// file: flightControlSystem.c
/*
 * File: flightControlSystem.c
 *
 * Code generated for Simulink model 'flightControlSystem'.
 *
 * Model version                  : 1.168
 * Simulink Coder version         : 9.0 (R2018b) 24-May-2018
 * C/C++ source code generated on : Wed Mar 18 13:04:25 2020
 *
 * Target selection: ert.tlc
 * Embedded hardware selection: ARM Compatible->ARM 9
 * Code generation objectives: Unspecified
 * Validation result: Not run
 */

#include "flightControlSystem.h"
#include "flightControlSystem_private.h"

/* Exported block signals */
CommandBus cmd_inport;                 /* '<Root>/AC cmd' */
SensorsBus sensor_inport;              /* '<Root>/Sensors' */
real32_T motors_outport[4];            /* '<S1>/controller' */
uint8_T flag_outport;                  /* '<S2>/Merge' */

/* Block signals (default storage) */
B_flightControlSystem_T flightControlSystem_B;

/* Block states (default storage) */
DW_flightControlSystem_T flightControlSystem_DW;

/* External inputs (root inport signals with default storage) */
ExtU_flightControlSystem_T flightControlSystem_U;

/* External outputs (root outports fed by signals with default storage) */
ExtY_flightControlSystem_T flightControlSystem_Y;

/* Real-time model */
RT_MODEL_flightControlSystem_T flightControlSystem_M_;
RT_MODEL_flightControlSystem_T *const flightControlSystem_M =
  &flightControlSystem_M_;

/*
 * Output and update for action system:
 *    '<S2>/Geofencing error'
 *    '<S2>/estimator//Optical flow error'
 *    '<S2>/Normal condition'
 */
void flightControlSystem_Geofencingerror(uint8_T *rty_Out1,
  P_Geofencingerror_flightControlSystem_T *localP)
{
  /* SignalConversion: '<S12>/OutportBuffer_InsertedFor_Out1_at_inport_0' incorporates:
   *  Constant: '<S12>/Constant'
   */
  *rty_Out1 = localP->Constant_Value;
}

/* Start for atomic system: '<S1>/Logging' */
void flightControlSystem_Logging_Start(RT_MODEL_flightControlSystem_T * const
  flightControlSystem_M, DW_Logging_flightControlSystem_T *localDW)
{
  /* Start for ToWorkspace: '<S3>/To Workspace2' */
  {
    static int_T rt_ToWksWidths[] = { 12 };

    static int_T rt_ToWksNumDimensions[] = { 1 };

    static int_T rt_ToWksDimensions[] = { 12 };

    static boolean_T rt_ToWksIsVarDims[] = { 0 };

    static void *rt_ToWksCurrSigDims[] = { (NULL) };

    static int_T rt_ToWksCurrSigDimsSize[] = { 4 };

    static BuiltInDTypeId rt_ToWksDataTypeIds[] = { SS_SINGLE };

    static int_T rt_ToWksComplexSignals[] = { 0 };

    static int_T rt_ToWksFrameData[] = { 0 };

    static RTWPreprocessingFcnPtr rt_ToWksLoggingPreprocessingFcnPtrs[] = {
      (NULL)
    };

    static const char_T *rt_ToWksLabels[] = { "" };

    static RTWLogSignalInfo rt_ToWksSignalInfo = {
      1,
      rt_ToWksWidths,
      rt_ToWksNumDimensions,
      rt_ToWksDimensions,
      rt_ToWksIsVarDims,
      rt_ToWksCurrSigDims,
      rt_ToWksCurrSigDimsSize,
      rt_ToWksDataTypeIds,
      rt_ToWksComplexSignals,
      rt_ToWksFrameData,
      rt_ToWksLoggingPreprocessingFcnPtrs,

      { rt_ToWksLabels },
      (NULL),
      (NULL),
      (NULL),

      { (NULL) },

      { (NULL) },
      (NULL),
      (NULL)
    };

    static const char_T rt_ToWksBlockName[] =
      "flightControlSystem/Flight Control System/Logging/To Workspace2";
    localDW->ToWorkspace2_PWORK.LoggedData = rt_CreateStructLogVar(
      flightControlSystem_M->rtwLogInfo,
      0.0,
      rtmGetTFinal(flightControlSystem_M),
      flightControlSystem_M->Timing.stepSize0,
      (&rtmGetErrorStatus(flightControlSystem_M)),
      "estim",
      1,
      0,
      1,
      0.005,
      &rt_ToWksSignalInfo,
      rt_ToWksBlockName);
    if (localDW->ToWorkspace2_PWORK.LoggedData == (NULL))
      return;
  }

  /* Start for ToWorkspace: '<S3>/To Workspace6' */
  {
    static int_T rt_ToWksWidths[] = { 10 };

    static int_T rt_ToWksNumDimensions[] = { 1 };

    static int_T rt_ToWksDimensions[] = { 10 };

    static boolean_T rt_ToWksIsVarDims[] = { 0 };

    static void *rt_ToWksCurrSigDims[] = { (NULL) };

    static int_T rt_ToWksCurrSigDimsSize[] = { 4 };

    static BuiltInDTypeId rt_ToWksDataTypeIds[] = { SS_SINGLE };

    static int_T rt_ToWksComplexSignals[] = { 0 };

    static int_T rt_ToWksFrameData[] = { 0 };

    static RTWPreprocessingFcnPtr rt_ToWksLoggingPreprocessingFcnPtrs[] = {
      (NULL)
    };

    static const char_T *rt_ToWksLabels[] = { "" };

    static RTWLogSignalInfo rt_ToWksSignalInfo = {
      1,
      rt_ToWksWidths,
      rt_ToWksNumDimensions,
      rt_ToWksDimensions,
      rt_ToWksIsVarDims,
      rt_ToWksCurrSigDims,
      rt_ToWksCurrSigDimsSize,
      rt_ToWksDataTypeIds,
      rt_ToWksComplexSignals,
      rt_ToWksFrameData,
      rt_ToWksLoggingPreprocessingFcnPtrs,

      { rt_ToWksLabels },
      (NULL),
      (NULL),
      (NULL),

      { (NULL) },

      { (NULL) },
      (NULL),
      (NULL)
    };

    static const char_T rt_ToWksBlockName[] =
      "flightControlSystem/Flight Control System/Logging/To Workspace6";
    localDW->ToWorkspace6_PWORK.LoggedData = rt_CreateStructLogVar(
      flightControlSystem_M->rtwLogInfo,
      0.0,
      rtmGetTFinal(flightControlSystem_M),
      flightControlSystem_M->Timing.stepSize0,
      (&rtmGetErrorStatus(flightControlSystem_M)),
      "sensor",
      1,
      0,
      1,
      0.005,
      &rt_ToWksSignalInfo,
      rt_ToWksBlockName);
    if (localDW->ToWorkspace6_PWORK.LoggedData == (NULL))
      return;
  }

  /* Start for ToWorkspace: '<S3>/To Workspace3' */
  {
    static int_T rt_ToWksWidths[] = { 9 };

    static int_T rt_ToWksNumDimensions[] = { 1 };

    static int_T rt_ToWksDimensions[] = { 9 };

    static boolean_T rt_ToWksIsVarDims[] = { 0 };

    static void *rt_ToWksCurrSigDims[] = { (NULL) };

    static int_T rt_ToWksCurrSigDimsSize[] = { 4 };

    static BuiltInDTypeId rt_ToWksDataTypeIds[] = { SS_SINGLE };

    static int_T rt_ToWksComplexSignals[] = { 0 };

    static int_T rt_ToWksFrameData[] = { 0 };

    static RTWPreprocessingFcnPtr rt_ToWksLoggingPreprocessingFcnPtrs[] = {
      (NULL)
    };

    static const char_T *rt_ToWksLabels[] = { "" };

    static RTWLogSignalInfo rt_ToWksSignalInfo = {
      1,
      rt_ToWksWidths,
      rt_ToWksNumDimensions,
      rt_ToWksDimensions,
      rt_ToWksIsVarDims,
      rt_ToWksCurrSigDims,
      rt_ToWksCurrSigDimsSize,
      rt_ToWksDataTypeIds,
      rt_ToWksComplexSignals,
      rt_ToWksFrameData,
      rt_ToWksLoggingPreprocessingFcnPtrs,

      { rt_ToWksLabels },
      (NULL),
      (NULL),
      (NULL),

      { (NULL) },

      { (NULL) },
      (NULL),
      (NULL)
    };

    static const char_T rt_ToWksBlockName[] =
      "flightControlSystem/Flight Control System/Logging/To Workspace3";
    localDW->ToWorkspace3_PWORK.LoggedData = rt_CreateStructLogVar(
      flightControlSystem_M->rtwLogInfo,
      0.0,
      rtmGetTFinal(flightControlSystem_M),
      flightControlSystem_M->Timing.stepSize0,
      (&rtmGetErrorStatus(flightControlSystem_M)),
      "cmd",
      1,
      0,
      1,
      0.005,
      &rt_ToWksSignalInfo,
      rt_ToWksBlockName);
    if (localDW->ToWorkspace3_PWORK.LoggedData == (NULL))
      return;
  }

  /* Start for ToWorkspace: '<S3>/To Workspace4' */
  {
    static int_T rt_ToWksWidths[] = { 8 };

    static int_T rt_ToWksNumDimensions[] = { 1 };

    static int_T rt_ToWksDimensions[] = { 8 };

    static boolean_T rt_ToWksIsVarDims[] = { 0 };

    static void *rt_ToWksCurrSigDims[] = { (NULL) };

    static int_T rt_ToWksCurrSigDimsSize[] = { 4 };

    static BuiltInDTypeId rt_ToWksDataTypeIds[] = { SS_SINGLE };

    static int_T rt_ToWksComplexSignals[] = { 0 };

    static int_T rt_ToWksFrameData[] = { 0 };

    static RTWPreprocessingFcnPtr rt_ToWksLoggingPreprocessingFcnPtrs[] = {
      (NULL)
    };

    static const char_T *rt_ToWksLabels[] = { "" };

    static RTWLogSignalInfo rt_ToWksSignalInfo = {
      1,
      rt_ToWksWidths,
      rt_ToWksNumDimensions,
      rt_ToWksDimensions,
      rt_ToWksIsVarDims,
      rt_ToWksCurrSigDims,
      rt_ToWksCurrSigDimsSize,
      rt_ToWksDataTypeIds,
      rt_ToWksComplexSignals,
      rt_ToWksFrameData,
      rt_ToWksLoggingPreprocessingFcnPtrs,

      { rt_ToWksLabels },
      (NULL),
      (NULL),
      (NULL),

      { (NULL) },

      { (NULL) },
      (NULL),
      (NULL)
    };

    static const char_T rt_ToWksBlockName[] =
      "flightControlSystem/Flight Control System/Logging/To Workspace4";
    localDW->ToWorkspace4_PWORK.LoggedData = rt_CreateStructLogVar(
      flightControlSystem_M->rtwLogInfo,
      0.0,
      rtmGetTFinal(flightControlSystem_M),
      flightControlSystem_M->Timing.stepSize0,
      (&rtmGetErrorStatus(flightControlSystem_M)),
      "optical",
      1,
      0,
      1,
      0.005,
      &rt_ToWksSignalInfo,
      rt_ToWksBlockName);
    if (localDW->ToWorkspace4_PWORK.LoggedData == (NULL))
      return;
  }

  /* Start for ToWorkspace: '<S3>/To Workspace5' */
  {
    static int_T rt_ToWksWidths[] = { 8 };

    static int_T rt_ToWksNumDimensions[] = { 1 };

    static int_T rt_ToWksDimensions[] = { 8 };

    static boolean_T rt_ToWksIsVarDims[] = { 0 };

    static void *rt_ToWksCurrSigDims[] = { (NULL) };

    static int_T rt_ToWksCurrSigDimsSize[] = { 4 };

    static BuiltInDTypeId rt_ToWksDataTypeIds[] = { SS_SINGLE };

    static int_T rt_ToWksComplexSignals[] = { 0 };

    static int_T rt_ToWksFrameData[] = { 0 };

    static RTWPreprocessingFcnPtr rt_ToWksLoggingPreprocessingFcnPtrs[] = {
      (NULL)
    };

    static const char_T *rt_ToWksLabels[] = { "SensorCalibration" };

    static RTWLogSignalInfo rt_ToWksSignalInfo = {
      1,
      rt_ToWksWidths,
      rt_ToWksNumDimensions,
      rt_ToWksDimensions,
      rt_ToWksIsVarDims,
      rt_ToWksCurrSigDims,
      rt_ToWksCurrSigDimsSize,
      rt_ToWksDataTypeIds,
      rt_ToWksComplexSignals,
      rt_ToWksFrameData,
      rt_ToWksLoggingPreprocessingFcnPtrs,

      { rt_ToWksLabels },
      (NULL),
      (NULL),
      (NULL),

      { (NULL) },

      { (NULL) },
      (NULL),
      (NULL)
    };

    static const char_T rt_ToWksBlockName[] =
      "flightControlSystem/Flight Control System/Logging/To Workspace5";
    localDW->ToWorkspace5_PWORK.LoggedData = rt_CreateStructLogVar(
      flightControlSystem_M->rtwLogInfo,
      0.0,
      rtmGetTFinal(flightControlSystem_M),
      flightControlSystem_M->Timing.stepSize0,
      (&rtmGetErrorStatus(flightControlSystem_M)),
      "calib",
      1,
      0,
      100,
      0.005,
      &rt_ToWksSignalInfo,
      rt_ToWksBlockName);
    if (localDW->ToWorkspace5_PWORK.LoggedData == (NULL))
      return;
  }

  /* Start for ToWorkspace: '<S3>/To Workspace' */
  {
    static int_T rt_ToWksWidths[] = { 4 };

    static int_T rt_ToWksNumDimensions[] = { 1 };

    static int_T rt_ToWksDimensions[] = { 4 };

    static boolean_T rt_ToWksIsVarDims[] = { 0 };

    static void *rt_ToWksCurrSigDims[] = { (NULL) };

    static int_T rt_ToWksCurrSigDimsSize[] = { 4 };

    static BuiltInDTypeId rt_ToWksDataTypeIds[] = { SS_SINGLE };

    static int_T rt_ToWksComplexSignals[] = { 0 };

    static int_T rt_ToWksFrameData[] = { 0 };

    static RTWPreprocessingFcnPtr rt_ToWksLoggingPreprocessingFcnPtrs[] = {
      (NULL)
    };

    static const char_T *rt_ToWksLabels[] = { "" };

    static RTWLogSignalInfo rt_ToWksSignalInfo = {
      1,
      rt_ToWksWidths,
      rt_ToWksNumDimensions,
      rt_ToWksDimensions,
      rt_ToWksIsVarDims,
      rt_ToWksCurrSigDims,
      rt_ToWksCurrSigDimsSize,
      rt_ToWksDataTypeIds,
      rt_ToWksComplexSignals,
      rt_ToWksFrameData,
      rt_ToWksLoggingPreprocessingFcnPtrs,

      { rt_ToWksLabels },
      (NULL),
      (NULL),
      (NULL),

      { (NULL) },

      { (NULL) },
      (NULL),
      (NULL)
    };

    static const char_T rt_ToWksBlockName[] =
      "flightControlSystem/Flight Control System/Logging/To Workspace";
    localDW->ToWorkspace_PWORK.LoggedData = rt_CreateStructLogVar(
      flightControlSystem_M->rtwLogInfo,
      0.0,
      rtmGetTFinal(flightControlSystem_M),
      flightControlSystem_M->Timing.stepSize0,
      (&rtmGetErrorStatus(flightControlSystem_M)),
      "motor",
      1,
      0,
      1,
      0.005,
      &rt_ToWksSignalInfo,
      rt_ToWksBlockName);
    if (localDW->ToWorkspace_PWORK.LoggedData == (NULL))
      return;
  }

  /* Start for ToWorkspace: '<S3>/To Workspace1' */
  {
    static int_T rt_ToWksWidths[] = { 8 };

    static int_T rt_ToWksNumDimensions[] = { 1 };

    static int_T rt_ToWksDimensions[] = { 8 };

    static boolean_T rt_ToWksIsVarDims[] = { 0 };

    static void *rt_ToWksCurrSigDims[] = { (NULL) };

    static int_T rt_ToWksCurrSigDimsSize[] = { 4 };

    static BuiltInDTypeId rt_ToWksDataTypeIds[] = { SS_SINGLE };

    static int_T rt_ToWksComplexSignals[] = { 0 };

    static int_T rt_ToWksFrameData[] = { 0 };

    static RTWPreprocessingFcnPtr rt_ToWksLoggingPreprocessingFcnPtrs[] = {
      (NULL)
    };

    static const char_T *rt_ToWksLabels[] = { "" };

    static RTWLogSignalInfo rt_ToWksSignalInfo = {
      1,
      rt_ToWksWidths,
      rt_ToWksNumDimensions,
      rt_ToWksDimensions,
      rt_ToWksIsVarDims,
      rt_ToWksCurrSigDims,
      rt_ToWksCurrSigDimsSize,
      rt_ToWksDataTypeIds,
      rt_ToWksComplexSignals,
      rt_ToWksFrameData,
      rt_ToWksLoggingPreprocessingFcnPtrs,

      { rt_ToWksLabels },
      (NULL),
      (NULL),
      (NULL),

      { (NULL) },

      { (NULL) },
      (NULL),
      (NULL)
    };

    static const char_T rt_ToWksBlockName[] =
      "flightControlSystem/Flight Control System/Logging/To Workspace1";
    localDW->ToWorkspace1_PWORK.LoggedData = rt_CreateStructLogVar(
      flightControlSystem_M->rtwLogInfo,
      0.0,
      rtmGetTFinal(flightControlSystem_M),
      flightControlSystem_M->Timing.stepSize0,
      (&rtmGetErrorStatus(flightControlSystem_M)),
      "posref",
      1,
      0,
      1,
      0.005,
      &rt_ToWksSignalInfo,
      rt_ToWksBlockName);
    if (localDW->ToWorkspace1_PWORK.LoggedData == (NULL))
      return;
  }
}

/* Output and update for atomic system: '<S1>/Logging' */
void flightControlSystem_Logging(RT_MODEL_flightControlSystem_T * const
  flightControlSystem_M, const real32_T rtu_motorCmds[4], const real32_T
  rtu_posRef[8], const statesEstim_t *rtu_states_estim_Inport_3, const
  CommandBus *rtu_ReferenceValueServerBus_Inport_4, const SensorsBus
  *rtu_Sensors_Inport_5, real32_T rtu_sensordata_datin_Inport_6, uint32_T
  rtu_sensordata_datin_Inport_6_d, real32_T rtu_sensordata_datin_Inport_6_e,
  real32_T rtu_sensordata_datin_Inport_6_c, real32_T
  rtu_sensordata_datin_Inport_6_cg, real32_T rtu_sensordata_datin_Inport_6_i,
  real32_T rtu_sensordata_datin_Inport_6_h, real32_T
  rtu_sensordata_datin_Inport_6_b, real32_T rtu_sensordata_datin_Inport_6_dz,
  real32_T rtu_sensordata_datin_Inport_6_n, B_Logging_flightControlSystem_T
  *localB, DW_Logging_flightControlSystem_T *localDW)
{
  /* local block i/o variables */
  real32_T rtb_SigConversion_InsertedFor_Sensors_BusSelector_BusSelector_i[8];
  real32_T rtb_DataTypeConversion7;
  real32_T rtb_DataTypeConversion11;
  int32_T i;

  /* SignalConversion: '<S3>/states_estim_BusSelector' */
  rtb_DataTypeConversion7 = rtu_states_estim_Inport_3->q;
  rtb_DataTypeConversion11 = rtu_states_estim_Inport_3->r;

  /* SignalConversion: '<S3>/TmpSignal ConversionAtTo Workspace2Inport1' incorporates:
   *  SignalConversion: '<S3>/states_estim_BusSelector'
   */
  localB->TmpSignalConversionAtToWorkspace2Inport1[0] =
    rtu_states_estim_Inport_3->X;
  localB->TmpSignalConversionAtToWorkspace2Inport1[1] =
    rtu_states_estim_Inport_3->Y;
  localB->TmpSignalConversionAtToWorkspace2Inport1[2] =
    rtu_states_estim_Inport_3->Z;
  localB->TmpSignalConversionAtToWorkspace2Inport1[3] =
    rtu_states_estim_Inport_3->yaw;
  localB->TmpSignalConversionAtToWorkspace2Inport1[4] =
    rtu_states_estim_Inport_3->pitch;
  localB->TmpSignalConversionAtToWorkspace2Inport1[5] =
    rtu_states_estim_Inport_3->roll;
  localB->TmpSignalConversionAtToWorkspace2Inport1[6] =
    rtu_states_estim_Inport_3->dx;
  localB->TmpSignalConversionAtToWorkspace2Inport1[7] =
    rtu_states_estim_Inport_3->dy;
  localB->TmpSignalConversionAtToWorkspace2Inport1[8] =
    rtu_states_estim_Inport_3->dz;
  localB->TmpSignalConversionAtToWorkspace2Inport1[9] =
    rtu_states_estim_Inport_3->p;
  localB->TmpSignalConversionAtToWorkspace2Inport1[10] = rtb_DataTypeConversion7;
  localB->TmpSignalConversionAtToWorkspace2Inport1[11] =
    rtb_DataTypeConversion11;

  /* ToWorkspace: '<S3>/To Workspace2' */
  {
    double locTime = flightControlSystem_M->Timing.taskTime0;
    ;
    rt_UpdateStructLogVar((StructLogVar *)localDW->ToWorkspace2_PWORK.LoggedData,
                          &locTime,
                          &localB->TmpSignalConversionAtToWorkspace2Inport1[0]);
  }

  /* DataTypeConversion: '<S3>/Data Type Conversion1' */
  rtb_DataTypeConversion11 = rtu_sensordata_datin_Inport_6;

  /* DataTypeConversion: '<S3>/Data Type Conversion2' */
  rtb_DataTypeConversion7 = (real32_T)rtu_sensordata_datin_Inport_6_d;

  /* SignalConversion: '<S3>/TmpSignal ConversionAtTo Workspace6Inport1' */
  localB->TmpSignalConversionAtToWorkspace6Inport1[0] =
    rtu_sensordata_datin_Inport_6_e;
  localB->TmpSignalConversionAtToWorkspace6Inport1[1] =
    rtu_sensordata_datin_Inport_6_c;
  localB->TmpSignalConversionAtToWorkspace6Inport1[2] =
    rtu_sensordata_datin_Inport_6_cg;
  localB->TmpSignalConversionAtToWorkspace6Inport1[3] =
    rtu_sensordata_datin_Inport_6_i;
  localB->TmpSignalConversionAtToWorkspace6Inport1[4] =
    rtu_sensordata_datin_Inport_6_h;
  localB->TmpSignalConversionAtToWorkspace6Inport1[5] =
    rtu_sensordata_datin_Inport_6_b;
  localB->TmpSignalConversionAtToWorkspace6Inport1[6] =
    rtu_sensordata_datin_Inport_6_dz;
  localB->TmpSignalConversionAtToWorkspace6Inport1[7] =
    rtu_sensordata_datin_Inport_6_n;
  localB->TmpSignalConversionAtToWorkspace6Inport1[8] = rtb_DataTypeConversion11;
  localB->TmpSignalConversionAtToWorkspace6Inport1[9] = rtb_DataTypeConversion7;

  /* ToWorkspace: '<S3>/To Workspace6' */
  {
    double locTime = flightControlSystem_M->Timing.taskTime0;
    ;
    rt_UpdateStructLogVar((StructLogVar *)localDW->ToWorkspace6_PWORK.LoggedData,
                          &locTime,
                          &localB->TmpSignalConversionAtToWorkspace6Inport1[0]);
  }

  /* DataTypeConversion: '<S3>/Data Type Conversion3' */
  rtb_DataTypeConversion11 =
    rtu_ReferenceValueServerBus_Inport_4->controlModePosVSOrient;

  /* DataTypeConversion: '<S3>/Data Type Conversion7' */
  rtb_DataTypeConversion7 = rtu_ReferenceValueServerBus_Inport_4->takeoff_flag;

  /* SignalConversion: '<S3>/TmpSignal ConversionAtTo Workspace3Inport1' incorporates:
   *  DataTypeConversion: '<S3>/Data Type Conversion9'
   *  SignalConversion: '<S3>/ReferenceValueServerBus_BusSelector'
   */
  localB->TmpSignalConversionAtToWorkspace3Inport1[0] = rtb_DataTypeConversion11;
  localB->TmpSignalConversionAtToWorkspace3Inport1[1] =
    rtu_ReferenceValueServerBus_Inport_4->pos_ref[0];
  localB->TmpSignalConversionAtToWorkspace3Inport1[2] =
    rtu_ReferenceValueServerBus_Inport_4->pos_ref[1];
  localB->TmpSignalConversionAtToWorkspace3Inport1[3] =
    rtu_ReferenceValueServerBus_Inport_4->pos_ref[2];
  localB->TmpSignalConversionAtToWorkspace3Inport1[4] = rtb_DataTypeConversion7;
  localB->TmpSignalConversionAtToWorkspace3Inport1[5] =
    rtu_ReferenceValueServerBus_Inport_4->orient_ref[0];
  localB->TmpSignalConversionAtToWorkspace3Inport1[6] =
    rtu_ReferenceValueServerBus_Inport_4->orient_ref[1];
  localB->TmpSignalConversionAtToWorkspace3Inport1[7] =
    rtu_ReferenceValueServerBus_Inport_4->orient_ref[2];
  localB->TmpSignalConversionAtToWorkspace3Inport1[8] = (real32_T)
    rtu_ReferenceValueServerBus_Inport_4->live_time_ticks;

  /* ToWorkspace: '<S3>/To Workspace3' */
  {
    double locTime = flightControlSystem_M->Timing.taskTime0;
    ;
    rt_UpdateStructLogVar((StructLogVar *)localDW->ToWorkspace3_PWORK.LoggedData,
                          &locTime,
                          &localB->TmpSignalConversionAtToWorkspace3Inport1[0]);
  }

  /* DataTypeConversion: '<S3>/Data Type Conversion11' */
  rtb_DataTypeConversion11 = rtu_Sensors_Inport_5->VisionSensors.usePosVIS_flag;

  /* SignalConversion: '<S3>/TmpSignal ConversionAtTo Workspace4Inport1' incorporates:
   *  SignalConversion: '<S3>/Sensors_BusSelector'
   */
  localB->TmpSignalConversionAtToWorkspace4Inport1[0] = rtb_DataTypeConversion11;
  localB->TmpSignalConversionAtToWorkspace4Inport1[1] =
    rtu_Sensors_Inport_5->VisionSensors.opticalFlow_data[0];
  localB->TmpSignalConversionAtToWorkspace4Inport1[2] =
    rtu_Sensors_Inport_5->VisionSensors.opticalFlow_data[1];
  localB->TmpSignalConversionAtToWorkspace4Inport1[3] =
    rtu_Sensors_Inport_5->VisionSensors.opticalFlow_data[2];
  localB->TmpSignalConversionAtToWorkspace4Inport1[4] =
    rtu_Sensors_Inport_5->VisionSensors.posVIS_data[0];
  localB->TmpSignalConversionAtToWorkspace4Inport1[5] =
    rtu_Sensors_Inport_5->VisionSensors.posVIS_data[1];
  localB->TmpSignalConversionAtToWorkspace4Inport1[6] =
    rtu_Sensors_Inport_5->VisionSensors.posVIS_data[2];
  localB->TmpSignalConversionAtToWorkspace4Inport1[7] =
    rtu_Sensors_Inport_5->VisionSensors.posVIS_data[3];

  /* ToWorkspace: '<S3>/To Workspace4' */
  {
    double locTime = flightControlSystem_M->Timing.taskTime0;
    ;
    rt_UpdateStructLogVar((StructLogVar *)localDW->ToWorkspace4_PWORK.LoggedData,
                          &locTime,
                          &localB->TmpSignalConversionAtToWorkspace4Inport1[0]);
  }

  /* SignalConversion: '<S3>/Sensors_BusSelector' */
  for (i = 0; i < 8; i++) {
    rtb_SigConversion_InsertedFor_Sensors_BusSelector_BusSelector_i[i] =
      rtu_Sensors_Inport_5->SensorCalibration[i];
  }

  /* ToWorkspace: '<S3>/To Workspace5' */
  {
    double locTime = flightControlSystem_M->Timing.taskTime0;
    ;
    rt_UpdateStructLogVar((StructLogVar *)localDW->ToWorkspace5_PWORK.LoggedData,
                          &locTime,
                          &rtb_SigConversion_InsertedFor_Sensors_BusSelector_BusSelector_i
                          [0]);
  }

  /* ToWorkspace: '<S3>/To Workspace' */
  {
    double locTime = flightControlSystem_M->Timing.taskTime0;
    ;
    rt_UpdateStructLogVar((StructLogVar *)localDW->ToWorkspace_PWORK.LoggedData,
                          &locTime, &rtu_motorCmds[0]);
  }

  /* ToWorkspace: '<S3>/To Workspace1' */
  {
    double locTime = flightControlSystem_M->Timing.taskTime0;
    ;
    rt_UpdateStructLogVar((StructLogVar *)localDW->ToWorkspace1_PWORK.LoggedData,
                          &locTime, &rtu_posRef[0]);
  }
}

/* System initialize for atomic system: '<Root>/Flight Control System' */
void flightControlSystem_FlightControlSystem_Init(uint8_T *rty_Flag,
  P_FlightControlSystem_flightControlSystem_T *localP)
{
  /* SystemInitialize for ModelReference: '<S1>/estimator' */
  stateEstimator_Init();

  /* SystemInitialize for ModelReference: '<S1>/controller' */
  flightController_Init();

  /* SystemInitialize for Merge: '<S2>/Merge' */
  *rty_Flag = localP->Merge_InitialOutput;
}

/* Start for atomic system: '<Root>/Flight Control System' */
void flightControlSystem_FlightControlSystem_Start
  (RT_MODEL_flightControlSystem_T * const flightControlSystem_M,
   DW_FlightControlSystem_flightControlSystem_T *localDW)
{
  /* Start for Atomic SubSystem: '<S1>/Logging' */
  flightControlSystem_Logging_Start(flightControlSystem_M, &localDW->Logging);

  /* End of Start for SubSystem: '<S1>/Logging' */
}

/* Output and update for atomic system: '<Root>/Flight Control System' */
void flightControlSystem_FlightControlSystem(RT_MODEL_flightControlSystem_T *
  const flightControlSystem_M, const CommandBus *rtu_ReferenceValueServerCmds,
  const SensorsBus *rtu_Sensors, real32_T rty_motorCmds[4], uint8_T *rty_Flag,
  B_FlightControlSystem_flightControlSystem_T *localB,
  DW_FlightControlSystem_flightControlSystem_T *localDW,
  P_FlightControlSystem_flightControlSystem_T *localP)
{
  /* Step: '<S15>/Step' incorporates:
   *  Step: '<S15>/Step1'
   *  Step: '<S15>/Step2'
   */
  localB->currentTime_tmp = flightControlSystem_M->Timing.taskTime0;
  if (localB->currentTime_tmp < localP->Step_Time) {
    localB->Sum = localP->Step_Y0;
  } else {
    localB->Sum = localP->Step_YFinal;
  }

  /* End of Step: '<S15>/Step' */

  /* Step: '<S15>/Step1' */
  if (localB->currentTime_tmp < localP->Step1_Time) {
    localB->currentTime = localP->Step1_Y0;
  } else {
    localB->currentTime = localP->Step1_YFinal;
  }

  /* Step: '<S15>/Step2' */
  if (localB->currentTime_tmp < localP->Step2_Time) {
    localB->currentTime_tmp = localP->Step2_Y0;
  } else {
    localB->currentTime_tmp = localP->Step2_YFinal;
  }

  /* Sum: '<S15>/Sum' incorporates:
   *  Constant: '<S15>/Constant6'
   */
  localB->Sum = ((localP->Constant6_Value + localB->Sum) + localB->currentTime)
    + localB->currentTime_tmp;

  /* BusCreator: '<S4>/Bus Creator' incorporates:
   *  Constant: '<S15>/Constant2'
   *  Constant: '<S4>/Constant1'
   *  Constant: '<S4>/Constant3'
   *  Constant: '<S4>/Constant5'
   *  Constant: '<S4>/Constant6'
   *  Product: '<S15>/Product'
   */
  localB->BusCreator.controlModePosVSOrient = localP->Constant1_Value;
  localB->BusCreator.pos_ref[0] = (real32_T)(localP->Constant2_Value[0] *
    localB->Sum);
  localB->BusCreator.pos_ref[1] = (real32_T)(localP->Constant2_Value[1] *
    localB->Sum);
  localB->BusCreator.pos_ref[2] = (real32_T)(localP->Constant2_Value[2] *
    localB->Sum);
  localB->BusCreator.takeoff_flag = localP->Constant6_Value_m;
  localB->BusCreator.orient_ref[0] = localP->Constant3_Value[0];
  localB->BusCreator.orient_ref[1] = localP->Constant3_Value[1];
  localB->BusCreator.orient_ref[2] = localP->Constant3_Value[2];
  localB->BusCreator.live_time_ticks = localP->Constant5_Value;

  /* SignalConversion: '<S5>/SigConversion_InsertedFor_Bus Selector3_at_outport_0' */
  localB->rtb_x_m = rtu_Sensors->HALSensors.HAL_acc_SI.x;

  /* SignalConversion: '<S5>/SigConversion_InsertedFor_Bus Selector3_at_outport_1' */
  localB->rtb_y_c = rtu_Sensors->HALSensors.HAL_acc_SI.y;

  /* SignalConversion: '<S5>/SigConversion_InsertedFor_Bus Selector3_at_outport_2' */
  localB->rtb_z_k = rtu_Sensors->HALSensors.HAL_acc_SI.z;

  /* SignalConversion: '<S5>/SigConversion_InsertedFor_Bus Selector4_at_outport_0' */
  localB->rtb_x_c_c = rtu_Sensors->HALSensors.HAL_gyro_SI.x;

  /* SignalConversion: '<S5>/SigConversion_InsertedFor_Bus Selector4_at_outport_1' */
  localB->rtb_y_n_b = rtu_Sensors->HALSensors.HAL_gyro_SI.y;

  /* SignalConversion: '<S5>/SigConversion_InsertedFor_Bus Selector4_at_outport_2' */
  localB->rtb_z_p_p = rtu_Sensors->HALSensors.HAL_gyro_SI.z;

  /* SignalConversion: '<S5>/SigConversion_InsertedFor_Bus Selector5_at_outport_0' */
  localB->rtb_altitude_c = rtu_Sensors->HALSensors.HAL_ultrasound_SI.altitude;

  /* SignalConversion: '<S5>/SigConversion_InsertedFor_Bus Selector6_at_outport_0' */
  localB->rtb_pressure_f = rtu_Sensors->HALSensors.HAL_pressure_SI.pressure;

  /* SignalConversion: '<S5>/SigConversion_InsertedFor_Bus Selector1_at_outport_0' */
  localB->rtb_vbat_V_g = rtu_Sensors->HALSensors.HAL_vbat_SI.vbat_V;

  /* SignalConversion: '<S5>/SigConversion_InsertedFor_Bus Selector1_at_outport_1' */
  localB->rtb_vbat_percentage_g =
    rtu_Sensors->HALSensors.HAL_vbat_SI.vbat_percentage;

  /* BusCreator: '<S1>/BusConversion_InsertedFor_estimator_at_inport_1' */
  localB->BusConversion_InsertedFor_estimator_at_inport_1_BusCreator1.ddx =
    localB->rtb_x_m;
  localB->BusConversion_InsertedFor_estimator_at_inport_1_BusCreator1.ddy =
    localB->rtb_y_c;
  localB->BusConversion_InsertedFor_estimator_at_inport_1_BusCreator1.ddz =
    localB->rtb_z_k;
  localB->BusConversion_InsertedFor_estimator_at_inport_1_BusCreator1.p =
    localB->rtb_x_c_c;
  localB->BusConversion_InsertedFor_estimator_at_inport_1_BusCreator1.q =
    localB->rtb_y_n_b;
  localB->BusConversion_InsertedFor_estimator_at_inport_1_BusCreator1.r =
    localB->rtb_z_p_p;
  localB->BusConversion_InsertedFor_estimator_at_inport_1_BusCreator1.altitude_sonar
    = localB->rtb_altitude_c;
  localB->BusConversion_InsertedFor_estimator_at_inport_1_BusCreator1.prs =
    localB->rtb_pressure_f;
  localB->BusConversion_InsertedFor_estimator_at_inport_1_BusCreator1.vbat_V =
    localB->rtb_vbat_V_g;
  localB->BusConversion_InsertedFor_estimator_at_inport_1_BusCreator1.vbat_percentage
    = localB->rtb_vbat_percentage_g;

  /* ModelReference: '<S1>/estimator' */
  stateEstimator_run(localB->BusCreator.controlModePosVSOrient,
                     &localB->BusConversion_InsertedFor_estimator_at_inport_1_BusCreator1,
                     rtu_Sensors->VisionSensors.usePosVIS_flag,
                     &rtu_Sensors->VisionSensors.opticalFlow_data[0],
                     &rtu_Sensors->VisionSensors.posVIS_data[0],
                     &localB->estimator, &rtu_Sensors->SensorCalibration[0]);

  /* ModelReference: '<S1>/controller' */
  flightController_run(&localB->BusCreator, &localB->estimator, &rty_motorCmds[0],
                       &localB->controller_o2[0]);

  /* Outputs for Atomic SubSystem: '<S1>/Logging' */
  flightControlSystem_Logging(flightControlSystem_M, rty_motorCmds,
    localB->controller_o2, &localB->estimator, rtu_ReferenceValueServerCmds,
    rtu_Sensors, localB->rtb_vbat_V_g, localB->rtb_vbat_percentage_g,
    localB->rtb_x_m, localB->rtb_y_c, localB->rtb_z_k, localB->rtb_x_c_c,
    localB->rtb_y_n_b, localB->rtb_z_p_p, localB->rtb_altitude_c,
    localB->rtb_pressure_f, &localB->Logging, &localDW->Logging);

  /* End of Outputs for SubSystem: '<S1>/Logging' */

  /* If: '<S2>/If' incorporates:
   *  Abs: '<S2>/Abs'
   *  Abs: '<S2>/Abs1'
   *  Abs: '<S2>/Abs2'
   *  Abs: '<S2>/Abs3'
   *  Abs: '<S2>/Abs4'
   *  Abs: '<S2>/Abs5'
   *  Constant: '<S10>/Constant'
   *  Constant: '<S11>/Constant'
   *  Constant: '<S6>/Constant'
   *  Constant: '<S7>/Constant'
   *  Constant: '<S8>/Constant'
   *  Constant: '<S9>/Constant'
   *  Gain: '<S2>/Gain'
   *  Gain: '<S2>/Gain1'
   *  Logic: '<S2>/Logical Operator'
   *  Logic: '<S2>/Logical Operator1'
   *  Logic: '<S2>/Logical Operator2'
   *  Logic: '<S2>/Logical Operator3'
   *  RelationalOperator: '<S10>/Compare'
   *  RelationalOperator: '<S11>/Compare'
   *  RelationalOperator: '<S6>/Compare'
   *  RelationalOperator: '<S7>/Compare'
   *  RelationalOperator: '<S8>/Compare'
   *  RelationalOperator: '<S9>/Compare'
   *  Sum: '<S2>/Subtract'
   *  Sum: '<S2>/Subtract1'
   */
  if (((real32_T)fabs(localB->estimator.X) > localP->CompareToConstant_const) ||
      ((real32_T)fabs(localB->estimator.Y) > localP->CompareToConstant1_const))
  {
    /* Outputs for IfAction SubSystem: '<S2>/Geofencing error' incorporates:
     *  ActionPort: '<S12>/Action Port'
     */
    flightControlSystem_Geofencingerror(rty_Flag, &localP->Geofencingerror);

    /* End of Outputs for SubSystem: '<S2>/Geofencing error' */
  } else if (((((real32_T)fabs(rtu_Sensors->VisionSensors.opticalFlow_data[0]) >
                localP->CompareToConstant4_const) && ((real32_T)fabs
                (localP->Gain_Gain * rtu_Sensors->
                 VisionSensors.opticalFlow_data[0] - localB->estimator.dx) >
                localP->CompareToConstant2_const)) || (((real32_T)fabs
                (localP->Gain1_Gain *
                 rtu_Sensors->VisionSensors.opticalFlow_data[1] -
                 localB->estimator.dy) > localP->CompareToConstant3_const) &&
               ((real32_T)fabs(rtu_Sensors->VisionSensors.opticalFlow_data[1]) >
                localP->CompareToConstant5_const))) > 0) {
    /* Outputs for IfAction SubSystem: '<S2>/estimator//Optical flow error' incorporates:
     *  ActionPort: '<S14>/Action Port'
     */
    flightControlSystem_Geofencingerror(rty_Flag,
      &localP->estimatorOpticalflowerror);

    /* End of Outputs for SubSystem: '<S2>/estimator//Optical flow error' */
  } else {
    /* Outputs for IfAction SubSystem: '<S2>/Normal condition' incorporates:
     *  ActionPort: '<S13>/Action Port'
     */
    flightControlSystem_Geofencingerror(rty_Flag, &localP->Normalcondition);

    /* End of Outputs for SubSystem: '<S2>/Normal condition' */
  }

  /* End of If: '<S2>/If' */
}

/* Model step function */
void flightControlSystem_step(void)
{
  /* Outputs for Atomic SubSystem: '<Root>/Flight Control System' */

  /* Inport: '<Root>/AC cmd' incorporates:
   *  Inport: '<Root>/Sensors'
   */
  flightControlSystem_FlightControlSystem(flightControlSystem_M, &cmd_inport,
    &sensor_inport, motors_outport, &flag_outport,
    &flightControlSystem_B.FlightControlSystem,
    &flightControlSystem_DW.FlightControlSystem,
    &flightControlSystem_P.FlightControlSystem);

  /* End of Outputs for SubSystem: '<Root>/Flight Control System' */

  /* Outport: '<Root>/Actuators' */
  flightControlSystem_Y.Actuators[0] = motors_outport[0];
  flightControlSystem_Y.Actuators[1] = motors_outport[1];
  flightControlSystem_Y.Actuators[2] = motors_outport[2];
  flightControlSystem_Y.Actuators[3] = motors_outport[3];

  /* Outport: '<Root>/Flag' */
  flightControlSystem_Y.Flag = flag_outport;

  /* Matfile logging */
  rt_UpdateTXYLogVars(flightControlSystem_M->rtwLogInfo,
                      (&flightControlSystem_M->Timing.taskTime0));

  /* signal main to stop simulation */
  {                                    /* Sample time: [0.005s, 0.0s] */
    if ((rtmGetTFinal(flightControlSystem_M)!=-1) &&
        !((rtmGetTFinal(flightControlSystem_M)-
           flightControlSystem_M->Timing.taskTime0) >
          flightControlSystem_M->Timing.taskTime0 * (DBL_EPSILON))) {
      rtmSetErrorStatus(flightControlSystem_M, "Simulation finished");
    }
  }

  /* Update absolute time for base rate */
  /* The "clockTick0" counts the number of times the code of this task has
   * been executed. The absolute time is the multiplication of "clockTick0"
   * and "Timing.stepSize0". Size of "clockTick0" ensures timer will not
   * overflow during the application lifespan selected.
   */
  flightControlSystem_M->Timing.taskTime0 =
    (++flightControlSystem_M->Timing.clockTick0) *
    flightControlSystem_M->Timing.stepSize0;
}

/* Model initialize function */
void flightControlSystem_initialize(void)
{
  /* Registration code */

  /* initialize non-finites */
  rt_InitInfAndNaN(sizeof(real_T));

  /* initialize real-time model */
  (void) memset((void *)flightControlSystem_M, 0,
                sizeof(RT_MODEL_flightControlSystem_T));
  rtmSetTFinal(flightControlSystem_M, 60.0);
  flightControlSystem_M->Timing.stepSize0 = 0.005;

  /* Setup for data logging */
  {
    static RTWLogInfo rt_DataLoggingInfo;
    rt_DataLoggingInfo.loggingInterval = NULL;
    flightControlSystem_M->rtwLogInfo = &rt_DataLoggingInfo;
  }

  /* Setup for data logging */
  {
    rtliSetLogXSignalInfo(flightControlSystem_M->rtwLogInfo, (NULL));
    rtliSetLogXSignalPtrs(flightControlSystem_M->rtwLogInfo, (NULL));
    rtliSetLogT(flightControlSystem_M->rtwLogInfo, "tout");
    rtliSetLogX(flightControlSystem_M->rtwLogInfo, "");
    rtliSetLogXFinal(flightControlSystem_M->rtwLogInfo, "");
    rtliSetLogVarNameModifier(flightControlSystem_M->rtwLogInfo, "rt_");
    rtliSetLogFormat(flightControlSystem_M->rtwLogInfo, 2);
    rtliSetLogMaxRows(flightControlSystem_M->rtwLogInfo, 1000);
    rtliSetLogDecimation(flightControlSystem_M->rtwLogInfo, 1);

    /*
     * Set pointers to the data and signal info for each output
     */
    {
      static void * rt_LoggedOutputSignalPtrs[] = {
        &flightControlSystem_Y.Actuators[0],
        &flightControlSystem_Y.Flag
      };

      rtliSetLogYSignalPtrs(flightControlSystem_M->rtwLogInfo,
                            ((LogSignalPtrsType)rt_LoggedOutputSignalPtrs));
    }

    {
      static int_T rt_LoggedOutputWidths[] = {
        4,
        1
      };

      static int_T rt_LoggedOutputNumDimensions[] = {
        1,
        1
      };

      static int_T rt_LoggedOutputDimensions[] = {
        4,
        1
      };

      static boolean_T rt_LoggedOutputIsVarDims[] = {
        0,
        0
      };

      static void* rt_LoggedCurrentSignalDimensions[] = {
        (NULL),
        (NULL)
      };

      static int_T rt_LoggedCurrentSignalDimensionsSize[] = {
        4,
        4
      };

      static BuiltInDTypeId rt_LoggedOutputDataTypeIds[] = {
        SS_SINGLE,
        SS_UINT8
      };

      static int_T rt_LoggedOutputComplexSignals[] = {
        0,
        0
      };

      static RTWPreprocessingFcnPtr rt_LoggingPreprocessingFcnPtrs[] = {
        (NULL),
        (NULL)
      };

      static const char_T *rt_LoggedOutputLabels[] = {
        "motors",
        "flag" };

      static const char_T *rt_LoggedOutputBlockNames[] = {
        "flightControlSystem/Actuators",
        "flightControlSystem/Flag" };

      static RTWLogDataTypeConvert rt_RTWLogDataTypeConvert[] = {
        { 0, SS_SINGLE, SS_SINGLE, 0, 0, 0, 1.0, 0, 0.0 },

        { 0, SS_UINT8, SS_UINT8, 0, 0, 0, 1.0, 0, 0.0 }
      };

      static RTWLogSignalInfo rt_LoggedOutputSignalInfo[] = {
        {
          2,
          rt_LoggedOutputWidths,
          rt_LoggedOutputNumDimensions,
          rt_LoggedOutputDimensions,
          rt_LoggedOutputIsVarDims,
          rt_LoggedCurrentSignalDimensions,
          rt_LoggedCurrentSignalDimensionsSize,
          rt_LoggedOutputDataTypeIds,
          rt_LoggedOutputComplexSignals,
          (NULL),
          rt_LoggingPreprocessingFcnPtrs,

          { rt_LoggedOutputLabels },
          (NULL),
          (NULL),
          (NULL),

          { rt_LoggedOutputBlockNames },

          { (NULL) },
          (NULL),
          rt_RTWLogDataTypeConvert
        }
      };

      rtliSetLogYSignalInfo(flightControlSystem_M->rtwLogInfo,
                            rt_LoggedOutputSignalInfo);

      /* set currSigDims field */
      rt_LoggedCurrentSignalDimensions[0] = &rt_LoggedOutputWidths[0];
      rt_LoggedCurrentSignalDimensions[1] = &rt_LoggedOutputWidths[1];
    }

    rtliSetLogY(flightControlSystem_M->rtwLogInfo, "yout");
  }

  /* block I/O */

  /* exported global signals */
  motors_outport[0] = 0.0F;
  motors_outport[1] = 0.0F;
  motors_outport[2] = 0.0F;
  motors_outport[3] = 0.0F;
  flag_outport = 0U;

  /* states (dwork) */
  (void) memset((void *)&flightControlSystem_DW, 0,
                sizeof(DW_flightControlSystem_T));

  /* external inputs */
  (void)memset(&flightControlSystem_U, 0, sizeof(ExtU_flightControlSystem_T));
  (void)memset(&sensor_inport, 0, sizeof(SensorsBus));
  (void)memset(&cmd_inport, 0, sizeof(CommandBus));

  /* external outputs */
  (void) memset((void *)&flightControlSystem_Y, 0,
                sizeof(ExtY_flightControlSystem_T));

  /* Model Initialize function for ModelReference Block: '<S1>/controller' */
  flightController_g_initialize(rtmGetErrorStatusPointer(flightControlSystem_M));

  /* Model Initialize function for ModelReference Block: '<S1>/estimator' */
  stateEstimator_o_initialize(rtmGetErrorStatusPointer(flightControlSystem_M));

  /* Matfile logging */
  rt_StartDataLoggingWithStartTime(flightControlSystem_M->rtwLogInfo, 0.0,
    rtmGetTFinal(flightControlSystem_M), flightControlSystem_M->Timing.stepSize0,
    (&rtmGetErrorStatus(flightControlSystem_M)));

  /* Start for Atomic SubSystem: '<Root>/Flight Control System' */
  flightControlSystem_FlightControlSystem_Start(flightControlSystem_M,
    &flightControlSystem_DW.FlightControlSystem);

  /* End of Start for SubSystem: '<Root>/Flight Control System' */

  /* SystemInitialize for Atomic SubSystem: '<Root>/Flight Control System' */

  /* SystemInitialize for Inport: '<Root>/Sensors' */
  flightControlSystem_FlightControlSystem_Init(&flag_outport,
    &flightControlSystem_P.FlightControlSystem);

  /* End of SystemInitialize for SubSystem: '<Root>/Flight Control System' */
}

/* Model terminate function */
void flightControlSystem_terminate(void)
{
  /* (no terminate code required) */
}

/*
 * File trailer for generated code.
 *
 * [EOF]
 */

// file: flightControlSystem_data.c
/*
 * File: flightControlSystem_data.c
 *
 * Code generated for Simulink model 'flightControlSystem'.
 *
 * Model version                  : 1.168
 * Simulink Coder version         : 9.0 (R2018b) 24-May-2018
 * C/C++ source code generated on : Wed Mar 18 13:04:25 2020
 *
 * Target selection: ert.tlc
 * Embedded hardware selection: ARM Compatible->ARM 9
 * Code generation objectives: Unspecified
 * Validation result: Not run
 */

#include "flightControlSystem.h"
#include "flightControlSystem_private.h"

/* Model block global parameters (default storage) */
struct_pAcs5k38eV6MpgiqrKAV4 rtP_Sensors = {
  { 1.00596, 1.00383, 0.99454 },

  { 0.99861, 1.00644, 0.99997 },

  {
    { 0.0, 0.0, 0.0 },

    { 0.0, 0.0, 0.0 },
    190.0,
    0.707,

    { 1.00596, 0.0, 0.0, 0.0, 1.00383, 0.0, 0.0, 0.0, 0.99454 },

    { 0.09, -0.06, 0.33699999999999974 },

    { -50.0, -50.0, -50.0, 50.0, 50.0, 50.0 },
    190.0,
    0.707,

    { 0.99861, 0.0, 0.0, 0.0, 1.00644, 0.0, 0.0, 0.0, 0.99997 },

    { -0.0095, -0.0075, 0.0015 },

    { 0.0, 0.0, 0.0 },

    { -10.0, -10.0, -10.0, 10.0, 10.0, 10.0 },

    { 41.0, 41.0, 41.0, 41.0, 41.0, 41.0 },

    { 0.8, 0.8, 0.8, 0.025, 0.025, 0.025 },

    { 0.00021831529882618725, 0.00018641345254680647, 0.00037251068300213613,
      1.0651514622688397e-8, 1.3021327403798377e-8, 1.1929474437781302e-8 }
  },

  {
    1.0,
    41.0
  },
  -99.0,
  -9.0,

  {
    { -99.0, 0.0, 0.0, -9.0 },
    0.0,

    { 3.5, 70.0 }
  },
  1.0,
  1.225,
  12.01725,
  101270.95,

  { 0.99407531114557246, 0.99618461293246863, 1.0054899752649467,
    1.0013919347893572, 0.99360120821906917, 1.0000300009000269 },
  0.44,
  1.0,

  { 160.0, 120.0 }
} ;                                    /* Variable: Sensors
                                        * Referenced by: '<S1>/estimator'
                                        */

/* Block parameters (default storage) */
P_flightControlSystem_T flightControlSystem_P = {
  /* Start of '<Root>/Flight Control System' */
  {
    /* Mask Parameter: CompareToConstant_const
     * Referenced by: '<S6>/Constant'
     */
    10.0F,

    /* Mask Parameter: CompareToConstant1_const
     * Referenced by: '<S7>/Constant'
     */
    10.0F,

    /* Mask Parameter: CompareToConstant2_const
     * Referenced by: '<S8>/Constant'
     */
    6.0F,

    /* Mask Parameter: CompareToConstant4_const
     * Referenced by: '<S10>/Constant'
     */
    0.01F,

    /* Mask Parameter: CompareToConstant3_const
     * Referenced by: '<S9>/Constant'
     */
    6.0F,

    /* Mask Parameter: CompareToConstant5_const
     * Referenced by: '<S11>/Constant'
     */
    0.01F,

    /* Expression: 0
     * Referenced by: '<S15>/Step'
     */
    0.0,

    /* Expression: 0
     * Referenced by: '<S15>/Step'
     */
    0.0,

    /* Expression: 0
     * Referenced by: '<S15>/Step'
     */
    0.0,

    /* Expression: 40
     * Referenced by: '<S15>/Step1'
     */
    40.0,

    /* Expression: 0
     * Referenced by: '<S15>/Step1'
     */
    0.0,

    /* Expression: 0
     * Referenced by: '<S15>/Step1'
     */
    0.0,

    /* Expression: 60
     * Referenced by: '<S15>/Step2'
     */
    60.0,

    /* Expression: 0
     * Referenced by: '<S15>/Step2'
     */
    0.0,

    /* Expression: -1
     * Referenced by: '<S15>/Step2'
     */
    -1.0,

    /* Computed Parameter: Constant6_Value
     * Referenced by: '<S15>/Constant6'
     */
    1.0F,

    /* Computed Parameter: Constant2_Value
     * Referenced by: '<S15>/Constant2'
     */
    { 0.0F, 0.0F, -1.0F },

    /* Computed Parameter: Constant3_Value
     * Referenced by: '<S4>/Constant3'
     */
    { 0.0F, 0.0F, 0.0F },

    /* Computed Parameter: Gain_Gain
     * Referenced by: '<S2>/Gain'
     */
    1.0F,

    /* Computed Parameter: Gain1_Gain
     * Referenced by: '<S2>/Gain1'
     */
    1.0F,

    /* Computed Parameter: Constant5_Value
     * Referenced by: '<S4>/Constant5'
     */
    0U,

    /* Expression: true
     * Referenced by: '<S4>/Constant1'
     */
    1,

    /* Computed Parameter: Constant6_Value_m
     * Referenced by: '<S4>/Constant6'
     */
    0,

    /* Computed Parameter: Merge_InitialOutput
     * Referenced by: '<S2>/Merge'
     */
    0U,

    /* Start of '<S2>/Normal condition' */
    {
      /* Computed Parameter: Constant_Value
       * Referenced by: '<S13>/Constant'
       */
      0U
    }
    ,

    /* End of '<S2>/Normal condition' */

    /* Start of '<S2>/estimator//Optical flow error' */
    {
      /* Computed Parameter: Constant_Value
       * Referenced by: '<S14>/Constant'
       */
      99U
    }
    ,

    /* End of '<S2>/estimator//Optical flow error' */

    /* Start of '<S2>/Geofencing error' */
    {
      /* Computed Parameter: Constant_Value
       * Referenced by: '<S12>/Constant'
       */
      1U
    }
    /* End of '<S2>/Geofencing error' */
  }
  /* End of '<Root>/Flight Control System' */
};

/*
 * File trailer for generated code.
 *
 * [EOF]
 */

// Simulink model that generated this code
simulink model "flightControlSystem"  (R2018b)
settings: Solver=ode3  StartTime=0  StopTime=60  FixedStep=Ts  RelTol=1e-3  EnableMultiTasking=on
undefined symbols (not defined in the file): Estimator, Ts
libraries: simulink x6

== system flightControlSystem ==
  note: Copyright 2013-2018 The MathWorks, Inc.
  note: Flight Control System
  AC cmd : Inport  OutDataTypeStr=Bus: CommandBus  BusOutputAsStruct=on
  Sensors : Inport  Port=2  OutDataTypeStr=Bus: SensorsBus  BusOutputAsStruct=on
  Image Data : Inport  Tag=IP_IN  Port=3  OutDataTypeStr=uint8  PortDimensions=[4 9600]  BusOutputAsStruct=on
  Flight Control System : Subsystem  TreatAsAtomicUnit=on  SystemSampleTime=Ts
  Terminator : Terminator
  Actuators : Outport  OutDataTypeStr=single  PortDimensions=4
  Flag : Outport  Port=2  OutDataTypeStr=uint8  PortDimensions=1
  wires:
  AC cmd/1 -> Flight Control System/1(ReferenceValueServerCmds)  "cmd"
  Flight Control System/1(motorCmds) -> Actuators/1  "motors"
  Sensors/1 -> Flight Control System/2(Sensors)  "sensors"
  Flight Control System/2(Flag) -> Flag/1  "flag"
  Image Data/1 -> Terminator/1  "Y1UY2V"

== system flightControlSystem/Flight Control System ==
  note: Derived from the work by Sertac
      | Karaman and Fabian Riether
  ReferenceValueServerCmds : Inport  OutDataTypeStr=Bus: CommandBus
  Sensors : Inport  Port=2  OutDataTypeStr=Bus: SensorsBus  BusOutputAsStruct=on
  Bus Selector : BusSelector  OutputSignals=VisionSensors.usePosVIS_flag,VisionSensors.opticalFlow_data,VisionSensors.posVIS_data,SensorCalibration
  Bus Selector1 : BusSelector  OutputSignals=controlModePosVSOrient
  Bus Selector2 : BusSelector  OutputSignals=HAL_acc_SI,HAL_gyro_SI,HAL_ultrasound_SI,HAL_pressure_SI,HAL_vbat_SI
  Bus Selector3 : BusSelector  OutputSignals=HALSensors
  Crash Predictor Flags : Subsystem
  Logging : Subsystem  TreatAsAtomicUnit=on
  Sensors1 : InportShadow  Port=2  OutDataTypeStr=Bus: SensorsBus  BusOutputAsStruct=on
  Sensors2 : InportShadow  Port=2  OutDataTypeStr=Bus: SensorsBus  BusOutputAsStruct=on
  Sensors3 : InportShadow  Port=2  OutDataTypeStr=Bus: SensorsBus  BusOutputAsStruct=on
  controller : ModelReference  ModelNameDialog=flightController.slx  SimulationMode=Normal  ModelReferenceVersion=1.361
  estimator : ModelReference  ModelNameDialog=stateEstimator.slx  SimulationMode=Normal  ModelReferenceVersion=1.43
  landing logic : Subsystem
  sensordata_group : Subsystem
  motorCmds : Outport
  Flag : Outport  Port=2
  wires:
  Bus Selector2/1 -> sensordata_group/1(HAL_acc_SI)  "<HAL_acc_SI>"
  Bus Selector2/2 -> sensordata_group/2(HAL_gyro_SI)  "<HAL_gyro_SI>"
  Bus Selector2/4 -> sensordata_group/4(HAL_pressure_SI)  "<HAL_pressure_SI>"
  Bus Selector2/3 -> sensordata_group/3(HAL_ultrasound_SI)  "<HAL_ultrasound_SI>"
  estimator/1 -> Crash Predictor Flags/1(states_estim), Logging/3(states_estim), controller/2
  Sensors2/1 -> Logging/5(Sensors)
  controller/2 -> Logging/2(posRef)
  ReferenceValueServerCmds/1 -> Logging/4(ReferenceValueServerBus)
  controller/1 -> Logging/1(motorCmds), motorCmds/1
  sensordata_group/1(sensordata_datin) -> Logging/6(sensordata_datin), estimator/2
  Bus Selector2/5 -> sensordata_group/5(HAL_vbat_SI)  "<HAL_vbat_SI>"
  Crash Predictor Flags/1(Flag) -> Flag/1
  Sensors/1 -> Bus Selector3/1
  Bus Selector3/1 -> Bus Selector2/1  "<HALSensors>"
  Sensors1/1 -> Bus Selector/1
  Bus Selector/1 -> estimator/3  "<usePosVIS_flag>"
  Bus Selector/2 -> estimator/4  "<opticalFlow_data>"
  Bus Selector/3 -> estimator/5  "<posVIS_data>"
  Bus Selector/4 -> estimator/6  "<SensorCalibration>"
  Bus Selector1/1 -> estimator/1  "<controlModePosVSOrient>"
  landing logic/1(ReferenceValueCmds) -> Bus Selector1/1, controller/1
  Sensors3/1 -> Crash Predictor Flags/2(Sensors)

== system flightControlSystem/Flight Control System/Crash Predictor Flags ==
  Bus Element In : Inport  PortName=states_estim  Element=X
  Bus Element In1 : Inport  PortName=states_estim  Element=Y
  Bus Element In2 : Inport  PortName=states_estim  Element=dx
  Bus Element In3 : Inport  PortName=states_estim  Element=dy
  Bus Element In4 : Inport  Port=2  PortName=Sensors  Element=VisionSensors.opticalFlow_data
  Abs{,1..5} (6 alike) : Abs
  Compare To Constant : simulink/Logic and Bit Operations/Compare To Constant  relop=>  const=10.0  OutDataTypeStr=boolean
  Compare To Constant1 : simulink/Logic and Bit Operations/Compare To Constant  relop=>  const=10.0  OutDataTypeStr=boolean
  Compare To Constant2 : simulink/Logic and Bit Operations/Compare To Constant  relop=>  const=6.0  OutDataTypeStr=boolean
  Compare To Constant3 : simulink/Logic and Bit Operations/Compare To Constant  relop=>  const=6.0  OutDataTypeStr=boolean
  Compare To Constant4 : simulink/Logic and Bit Operations/Compare To Constant  relop=>  const=0.01  OutDataTypeStr=boolean
  Compare To Constant5 : simulink/Logic and Bit Operations/Compare To Constant  relop=>  const=0.01  OutDataTypeStr=boolean
  Data Type Conversion : DataTypeConversion  OutDataTypeStr=uint8  RndMeth=Nearest
  Data Type Conversion1 : DataTypeConversion  OutDataTypeStr=uint8  RndMeth=Nearest
  Demux : Demux  Outputs=3
  Gain : Gain  Gain=Estimator.pos.visDeltaXYMax
  Gain1 : Gain  Gain=Estimator.pos.visDeltaXYMax
  Geofencing error : Subsystem  TreatAsAtomicUnit=on
  If : If  NumInputs=2  ElseIfExpressions=u2 > 0
  Logical Operator : Logic  Operator=OR  AllPortsSameDT=off
  Logical Operator1 : Logic  AllPortsSameDT=off  OutDataTypeStr=boolean
  Logical Operator2 : Logic  AllPortsSameDT=off  OutDataTypeStr=boolean
  Logical Operator3 : Logic  Operator=OR  AllPortsSameDT=off
  Merge : Merge  Inputs=3  InitialOutput=0
  Normal condition : Subsystem  TreatAsAtomicUnit=on
  Subtract : Sum  Inputs=-+
  Subtract1 : Sum  Inputs=-+
  Terminator : Terminator
  estimator/Optical flow error : Subsystem  TreatAsAtomicUnit=on
  Flag : Outport
  wires:
  Bus Element In/1 -> Abs/1
  Bus Element In1/1 -> Abs1/1
  Compare To Constant/1 -> Logical Operator/1
  Compare To Constant1/1 -> Logical Operator/2
  Abs/1 -> Compare To Constant/1
  Abs1/1 -> Compare To Constant1/1
  Logical Operator/1 -> Data Type Conversion/1
  Demux/1 -> Abs4/1, Gain/1
  Demux/2 -> Gain1/1, Abs5/1
  Bus Element In2/1 -> Subtract/1
  Subtract/1 -> Abs2/1
  Subtract1/1 -> Abs3/1
  Abs2/1 -> Compare To Constant2/1
  Abs3/1 -> Compare To Constant3/1
  Compare To Constant5/1 -> Logical Operator2/2
  Abs4/1 -> Compare To Constant4/1
  Abs5/1 -> Compare To Constant5/1
  Compare To Constant3/1 -> Logical Operator2/1
  Logical Operator1/1 -> Logical Operator3/1
  Logical Operator2/1 -> Logical Operator3/2
  Logical Operator3/1 -> Data Type Conversion1/1
  Demux/3 -> Terminator/1
  Gain/1 -> Subtract/2
  Bus Element In3/1 -> Subtract1/1
  Gain1/1 -> Subtract1/2
  Compare To Constant4/1 -> Logical Operator1/1
  Compare To Constant2/1 -> Logical Operator1/2
  Merge/1 -> Flag/1
  If/1 -> Geofencing error/Action
  If/2 -> estimator/Optical flow error/Action
  If/3 -> Normal condition/Action
  Geofencing error/1(Out1) -> Merge/1
  estimator/Optical flow error/1(Out1) -> Merge/2
  Normal condition/1(Out1) -> Merge/3
  Data Type Conversion/1 -> If/1
  Data Type Conversion1/1 -> If/2
  Bus Element In4/1 -> Demux/1

== system flightControlSystem/Flight Control System/Logging ==
  motorCmds : Inport
  posRef : Inport  Port=2
  Bus Element In : Inport  Port=3  PortName=states_estim  Element=X
  Bus Element In1 : Inport  Port=3  PortName=states_estim  Element=Y
  Bus Element In2 : Inport  Port=3  PortName=states_estim  Element=Z
  Bus Element In3 : Inport  Port=3  PortName=states_estim  Element=yaw
  Bus Element In6 : Inport  Port=3  PortName=states_estim  Element=dx
  Bus Element In5 : Inport  Port=3  PortName=states_estim  Element=roll
  Bus Element In4 : Inport  Port=3  PortName=states_estim  Element=pitch
  Bus Element In7 : Inport  Port=3  PortName=states_estim  Element=dy
  Bus Element In8 : Inport  Port=3  PortName=states_estim  Element=dz
  Bus Element In9 : Inport  Port=3  PortName=states_estim  Element=p
  Bus Element In10 : Inport  Port=3  PortName=states_estim  Element=q
  Bus Element In11 : Inport  Port=3  PortName=states_estim  Element=r
  Bus Element In12 : Inport  Port=4  PortName=ReferenceValueServerBus  Element=controlModePosVSOrient
  Bus Element In13 : Inport  Port=4  PortName=ReferenceValueServerBus  Element=pos_ref
  Bus Element In14 : Inport  Port=4  PortName=ReferenceValueServerBus  Element=takeoff_flag
  Bus Element In15 : Inport  Port=4  PortName=ReferenceValueServerBus  Element=orient_ref
  Bus Element In16 : Inport  Port=4  PortName=ReferenceValueServerBus  Element=live_time_ticks
  Bus Element In17 : Inport  Port=5  PortName=Sensors  Element=VisionSensors.usePosVIS_flag
  Bus Element In18 : Inport  Port=5  PortName=Sensors  Element=VisionSensors.opticalFlow_data
  Bus Element In19 : Inport  Port=5  PortName=Sensors  Element=VisionSensors.posVIS_data
  Bus Element In20 : Inport  Port=5  PortName=Sensors  Element=SensorCalibration
  Bus Element In21 : Inport  Port=6  PortName=sensordata_datin  Element=ddx
  Bus Element In22 : Inport  Port=6  PortName=sensordata_datin  Element=ddy
  Bus Element In23 : Inport  Port=6  PortName=sensordata_datin  Element=ddz
  Bus Element In24 : Inport  Port=6  PortName=sensordata_datin  Element=p
  Bus Element In25 : Inport  Port=6  PortName=sensordata_datin  Element=q
  Bus Element In26 : Inport  Port=6  PortName=sensordata_datin  Element=r
  Bus Element In27 : Inport  Port=6  PortName=sensordata_datin  Element=altitude_sonar
  Bus Element In28 : Inport  Port=6  PortName=sensordata_datin  Element=prs
  Bus Element In29 : Inport  Port=6  PortName=sensordata_datin  Element=vbat_percentage
  Bus Element In30 : Inport  Port=6  PortName=sensordata_datin  Element=vbat_V
  Data Type Conversion{1..3,7,9,11} (6 alike) : DataTypeConversion  OutDataTypeStr=single
  Mux : Mux  Inputs=3
  Mux1 : Mux  Inputs=5
  Mux2 : Mux  Inputs=12
  Mux3 : Mux  Inputs=10
  To Workspace : ToWorkspace  VariableName=motor  SaveFormat=Structure With Time  SampleTime=-1
  To Workspace1 : ToWorkspace  VariableName=posref  SaveFormat=Structure With Time  SampleTime=-1
  To Workspace2 : ToWorkspace  VariableName=estim  SaveFormat=Structure With Time  SampleTime=-1
  To Workspace3 : ToWorkspace  VariableName=cmd  SaveFormat=Structure With Time  SampleTime=-1
  To Workspace4 : ToWorkspace  VariableName=optical  SaveFormat=Structure With Time  SampleTime=-1
  To Workspace5 : ToWorkspace  VariableName=calib  SaveFormat=Structure With Time  SampleTime=-1
  To Workspace6 : ToWorkspace  VariableName=sensor  SaveFormat=Structure With Time  SampleTime=-1
  wires:
  Bus Element In12/1 -> Data Type Conversion3/1
  Bus Element In14/1 -> Data Type Conversion7/1
  Bus Element In16/1 -> Data Type Conversion9/1
  Bus Element In17/1 -> Data Type Conversion11/1
  Bus Element In20/1 -> To Workspace5/1
  Mux/1 -> To Workspace4/1
  Mux2/1 -> To Workspace2/1
  motorCmds/1 -> To Workspace/1
  Mux1/1 -> To Workspace3/1
  Bus Element In3/1 -> Mux2/4
  Bus Element In5/1 -> Mux2/6
  Bus Element In4/1 -> Mux2/5
  Bus Element In8/1 -> Mux2/9
  Bus Element In6/1 -> Mux2/7
  Bus Element In7/1 -> Mux2/8
  Bus Element In9/1 -> Mux2/10
  Bus Element In11/1 -> Mux2/12
  Bus Element In1/1 -> Mux2/2
  Bus Element In10/1 -> Mux2/11
  Bus Element In2/1 -> Mux2/3
  Bus Element In/1 -> Mux2/1
  Data Type Conversion3/1 -> Mux1/1
  Bus Element In13/1 -> Mux1/2
  Data Type Conversion7/1 -> Mux1/3
  Bus Element In15/1 -> Mux1/4
  Data Type Conversion9/1 -> Mux1/5
  Bus Element In19/1 -> Mux/3
  Bus Element In18/1 -> Mux/2
  Data Type Conversion11/1 -> Mux/1
  posRef/1 -> To Workspace1/1
  Bus Element In21/1 -> Mux3/1
  Bus Element In22/1 -> Mux3/2
  Bus Element In23/1 -> Mux3/3
  Bus Element In24/1 -> Mux3/4
  Bus Element In25/1 -> Mux3/5
  Bus Element In26/1 -> Mux3/6
  Bus Element In27/1 -> Mux3/7
  Bus Element In28/1 -> Mux3/8
  Bus Element In30/1 -> Data Type Conversion1/1
  Bus Element In29/1 -> Data Type Conversion2/1
  Mux3/1 -> To Workspace6/1
  Data Type Conversion1/1 -> Mux3/9
  Data Type Conversion2/1 -> Mux3/10

== system flightControlSystem/Flight Control System/landing logic ==
  Bus Creator : BusCreator  Inputs=5  OutDataTypeStr=Bus: CommandBus  NonVirtualBus=on
  Constant1 : Constant  Value=true  OutDataTypeStr=boolean
  Constant3 : Constant  Value=[0 0 0]  OutDataTypeStr=single
  Constant5 : Constant  Value=0  OutDataTypeStr=uint32
  Constant6 : Constant  Value=0  OutDataTypeStr=boolean
  Subsystem : Subsystem
  ReferenceValueCmds : Outport  OutDataTypeStr=Bus: CommandBus
  wires:
  Constant5/1 -> Bus Creator/5  "live_time_ticks"
  Bus Creator/1 -> ReferenceValueCmds/1
  Constant1/1 -> Bus Creator/1  "controlModePosVSOrient"
  Subsystem/1(pos_ref) -> Bus Creator/2  "pos_ref"
  Constant6/1 -> Bus Creator/3  "takeoff_flag"
  Constant3/1 -> Bus Creator/4  "orient_ref"

== system flightControlSystem/Flight Control System/sensordata_group ==
  HAL_acc_SI : Inport  OutDataTypeStr=Bus: HAL_acc_SI_t
  HAL_gyro_SI : Inport  Port=2  OutDataTypeStr=Bus: HAL_gyro_SI_t
  HAL_ultrasound_SI : Inport  Port=3  OutDataTypeStr=Bus: HAL_ultrasound_SI_t
  HAL_pressure_SI : Inport  Port=4  OutDataTypeStr=Bus: HAL_pressure_SI_t
  HAL_vbat_SI : Inport  Port=5  OutDataTypeStr=Bus: HAL_vbat_SI_t
  Bus Selector1 : BusSelector  OutputSignals=vbat_V,vbat_percentage
  Bus Selector3 : BusSelector  OutputSignals=x,y,z
  Bus Selector4 : BusSelector  OutputSignals=x,y,z
  Bus Selector5 : BusSelector  OutputSignals=altitude
  Bus Selector6 : BusSelector  OutputSignals=pressure
  Out Bus Element : Outport  PortName=sensordata_datin  Element=ddx
  Out Bus Element1 : Outport  PortName=sensordata_datin  Element=ddy
  Out Bus Element2 : Outport  PortName=sensordata_datin  Element=ddz
  Out Bus Element3 : Outport  PortName=sensordata_datin  Element=p
  Out Bus Element4 : Outport  PortName=sensordata_datin  Element=q
  Out Bus Element5 : Outport  PortName=sensordata_datin  Element=r
  Out Bus Element6 : Outport  PortName=sensordata_datin  Element=altitude_sonar
  Out Bus Element7 : Outport  PortName=sensordata_datin  Element=prs
  Out Bus Element8 : Outport  PortName=sensordata_datin  Element=vbat_V
  Out Bus Element9 : Outport  PortName=sensordata_datin  Element=vbat_percentage
  wires:
  HAL_gyro_SI/1 -> Bus Selector4/1
  HAL_acc_SI/1 -> Bus Selector3/1
  HAL_pressure_SI/1 -> Bus Selector6/1
  HAL_ultrasound_SI/1 -> Bus Selector5/1
  Bus Selector4/1 -> Out Bus Element3/1  "<x>"
  Bus Selector3/3 -> Out Bus Element2/1  "<z>"
  Bus Selector4/3 -> Out Bus Element5/1  "<z>"
  Bus Selector6/1 -> Out Bus Element7/1  "<pressure>"
  Bus Selector4/2 -> Out Bus Element4/1  "<y>"
  Bus Selector3/1 -> Out Bus Element/1  "<x>"
  Bus Selector3/2 -> Out Bus Element1/1  "<y>"
  Bus Selector1/1 -> Out Bus Element8/1  "<vbat_V>"
  HAL_vbat_SI/1 -> Bus Selector1/1
  Bus Selector1/2 -> Out Bus Element9/1  "<vbat_percentage>"
  Bus Selector5/1 -> Out Bus Element6/1  "<altitude>"

== system flightControlSystem/Flight Control System/Crash Predictor Flags/Geofencing error ==
  Action Port : ActionPort  ActionType=then
  Constant : Constant  OutDataTypeStr=uint8
  Out1 : Outport
  wires:
  Constant/1 -> Out1/1

== system flightControlSystem/Flight Control System/Crash Predictor Flags/Normal condition ==
  Action Port : ActionPort  ActionType=else
  Constant : Constant  Value=0  OutDataTypeStr=uint8
  Out1 : Outport
  wires:
  Constant/1 -> Out1/1

== system flightControlSystem/Flight Control System/Crash Predictor Flags/estimator//Optical flow error ==
  Action Port : ActionPort  ActionType=elseif
  Constant : Constant  Value=99  OutDataTypeStr=uint8
  Out1 : Outport
  wires:
  Constant/1 -> Out1/1

== system flightControlSystem/Flight Control System/landing logic/Subsystem ==
  Constant2 : Constant  Value=[0 0 -1]  OutDataTypeStr=single
  Constant6 : Constant  OutDataTypeStr=single
  Product : Product  OutDataTypeStr=single
  Step : Step  Time=0  After=0
  Step1 : Step  Time=40  After=0
  Step2 : Step  Time=60  After=-1
  Sum : Sum  Inputs=|++++
  pos_ref : Outport
  wires:
  Constant6/1 -> Sum/1
  Sum/1 -> Product/2
  Constant2/1 -> Product/1  "pos_ref"
  Step2/1 -> Sum/4
  Step1/1 -> Sum/3
  Product/1 -> pos_ref/1  "pos_ref"
  Step/1 -> Sum/2  "pos_ref"
